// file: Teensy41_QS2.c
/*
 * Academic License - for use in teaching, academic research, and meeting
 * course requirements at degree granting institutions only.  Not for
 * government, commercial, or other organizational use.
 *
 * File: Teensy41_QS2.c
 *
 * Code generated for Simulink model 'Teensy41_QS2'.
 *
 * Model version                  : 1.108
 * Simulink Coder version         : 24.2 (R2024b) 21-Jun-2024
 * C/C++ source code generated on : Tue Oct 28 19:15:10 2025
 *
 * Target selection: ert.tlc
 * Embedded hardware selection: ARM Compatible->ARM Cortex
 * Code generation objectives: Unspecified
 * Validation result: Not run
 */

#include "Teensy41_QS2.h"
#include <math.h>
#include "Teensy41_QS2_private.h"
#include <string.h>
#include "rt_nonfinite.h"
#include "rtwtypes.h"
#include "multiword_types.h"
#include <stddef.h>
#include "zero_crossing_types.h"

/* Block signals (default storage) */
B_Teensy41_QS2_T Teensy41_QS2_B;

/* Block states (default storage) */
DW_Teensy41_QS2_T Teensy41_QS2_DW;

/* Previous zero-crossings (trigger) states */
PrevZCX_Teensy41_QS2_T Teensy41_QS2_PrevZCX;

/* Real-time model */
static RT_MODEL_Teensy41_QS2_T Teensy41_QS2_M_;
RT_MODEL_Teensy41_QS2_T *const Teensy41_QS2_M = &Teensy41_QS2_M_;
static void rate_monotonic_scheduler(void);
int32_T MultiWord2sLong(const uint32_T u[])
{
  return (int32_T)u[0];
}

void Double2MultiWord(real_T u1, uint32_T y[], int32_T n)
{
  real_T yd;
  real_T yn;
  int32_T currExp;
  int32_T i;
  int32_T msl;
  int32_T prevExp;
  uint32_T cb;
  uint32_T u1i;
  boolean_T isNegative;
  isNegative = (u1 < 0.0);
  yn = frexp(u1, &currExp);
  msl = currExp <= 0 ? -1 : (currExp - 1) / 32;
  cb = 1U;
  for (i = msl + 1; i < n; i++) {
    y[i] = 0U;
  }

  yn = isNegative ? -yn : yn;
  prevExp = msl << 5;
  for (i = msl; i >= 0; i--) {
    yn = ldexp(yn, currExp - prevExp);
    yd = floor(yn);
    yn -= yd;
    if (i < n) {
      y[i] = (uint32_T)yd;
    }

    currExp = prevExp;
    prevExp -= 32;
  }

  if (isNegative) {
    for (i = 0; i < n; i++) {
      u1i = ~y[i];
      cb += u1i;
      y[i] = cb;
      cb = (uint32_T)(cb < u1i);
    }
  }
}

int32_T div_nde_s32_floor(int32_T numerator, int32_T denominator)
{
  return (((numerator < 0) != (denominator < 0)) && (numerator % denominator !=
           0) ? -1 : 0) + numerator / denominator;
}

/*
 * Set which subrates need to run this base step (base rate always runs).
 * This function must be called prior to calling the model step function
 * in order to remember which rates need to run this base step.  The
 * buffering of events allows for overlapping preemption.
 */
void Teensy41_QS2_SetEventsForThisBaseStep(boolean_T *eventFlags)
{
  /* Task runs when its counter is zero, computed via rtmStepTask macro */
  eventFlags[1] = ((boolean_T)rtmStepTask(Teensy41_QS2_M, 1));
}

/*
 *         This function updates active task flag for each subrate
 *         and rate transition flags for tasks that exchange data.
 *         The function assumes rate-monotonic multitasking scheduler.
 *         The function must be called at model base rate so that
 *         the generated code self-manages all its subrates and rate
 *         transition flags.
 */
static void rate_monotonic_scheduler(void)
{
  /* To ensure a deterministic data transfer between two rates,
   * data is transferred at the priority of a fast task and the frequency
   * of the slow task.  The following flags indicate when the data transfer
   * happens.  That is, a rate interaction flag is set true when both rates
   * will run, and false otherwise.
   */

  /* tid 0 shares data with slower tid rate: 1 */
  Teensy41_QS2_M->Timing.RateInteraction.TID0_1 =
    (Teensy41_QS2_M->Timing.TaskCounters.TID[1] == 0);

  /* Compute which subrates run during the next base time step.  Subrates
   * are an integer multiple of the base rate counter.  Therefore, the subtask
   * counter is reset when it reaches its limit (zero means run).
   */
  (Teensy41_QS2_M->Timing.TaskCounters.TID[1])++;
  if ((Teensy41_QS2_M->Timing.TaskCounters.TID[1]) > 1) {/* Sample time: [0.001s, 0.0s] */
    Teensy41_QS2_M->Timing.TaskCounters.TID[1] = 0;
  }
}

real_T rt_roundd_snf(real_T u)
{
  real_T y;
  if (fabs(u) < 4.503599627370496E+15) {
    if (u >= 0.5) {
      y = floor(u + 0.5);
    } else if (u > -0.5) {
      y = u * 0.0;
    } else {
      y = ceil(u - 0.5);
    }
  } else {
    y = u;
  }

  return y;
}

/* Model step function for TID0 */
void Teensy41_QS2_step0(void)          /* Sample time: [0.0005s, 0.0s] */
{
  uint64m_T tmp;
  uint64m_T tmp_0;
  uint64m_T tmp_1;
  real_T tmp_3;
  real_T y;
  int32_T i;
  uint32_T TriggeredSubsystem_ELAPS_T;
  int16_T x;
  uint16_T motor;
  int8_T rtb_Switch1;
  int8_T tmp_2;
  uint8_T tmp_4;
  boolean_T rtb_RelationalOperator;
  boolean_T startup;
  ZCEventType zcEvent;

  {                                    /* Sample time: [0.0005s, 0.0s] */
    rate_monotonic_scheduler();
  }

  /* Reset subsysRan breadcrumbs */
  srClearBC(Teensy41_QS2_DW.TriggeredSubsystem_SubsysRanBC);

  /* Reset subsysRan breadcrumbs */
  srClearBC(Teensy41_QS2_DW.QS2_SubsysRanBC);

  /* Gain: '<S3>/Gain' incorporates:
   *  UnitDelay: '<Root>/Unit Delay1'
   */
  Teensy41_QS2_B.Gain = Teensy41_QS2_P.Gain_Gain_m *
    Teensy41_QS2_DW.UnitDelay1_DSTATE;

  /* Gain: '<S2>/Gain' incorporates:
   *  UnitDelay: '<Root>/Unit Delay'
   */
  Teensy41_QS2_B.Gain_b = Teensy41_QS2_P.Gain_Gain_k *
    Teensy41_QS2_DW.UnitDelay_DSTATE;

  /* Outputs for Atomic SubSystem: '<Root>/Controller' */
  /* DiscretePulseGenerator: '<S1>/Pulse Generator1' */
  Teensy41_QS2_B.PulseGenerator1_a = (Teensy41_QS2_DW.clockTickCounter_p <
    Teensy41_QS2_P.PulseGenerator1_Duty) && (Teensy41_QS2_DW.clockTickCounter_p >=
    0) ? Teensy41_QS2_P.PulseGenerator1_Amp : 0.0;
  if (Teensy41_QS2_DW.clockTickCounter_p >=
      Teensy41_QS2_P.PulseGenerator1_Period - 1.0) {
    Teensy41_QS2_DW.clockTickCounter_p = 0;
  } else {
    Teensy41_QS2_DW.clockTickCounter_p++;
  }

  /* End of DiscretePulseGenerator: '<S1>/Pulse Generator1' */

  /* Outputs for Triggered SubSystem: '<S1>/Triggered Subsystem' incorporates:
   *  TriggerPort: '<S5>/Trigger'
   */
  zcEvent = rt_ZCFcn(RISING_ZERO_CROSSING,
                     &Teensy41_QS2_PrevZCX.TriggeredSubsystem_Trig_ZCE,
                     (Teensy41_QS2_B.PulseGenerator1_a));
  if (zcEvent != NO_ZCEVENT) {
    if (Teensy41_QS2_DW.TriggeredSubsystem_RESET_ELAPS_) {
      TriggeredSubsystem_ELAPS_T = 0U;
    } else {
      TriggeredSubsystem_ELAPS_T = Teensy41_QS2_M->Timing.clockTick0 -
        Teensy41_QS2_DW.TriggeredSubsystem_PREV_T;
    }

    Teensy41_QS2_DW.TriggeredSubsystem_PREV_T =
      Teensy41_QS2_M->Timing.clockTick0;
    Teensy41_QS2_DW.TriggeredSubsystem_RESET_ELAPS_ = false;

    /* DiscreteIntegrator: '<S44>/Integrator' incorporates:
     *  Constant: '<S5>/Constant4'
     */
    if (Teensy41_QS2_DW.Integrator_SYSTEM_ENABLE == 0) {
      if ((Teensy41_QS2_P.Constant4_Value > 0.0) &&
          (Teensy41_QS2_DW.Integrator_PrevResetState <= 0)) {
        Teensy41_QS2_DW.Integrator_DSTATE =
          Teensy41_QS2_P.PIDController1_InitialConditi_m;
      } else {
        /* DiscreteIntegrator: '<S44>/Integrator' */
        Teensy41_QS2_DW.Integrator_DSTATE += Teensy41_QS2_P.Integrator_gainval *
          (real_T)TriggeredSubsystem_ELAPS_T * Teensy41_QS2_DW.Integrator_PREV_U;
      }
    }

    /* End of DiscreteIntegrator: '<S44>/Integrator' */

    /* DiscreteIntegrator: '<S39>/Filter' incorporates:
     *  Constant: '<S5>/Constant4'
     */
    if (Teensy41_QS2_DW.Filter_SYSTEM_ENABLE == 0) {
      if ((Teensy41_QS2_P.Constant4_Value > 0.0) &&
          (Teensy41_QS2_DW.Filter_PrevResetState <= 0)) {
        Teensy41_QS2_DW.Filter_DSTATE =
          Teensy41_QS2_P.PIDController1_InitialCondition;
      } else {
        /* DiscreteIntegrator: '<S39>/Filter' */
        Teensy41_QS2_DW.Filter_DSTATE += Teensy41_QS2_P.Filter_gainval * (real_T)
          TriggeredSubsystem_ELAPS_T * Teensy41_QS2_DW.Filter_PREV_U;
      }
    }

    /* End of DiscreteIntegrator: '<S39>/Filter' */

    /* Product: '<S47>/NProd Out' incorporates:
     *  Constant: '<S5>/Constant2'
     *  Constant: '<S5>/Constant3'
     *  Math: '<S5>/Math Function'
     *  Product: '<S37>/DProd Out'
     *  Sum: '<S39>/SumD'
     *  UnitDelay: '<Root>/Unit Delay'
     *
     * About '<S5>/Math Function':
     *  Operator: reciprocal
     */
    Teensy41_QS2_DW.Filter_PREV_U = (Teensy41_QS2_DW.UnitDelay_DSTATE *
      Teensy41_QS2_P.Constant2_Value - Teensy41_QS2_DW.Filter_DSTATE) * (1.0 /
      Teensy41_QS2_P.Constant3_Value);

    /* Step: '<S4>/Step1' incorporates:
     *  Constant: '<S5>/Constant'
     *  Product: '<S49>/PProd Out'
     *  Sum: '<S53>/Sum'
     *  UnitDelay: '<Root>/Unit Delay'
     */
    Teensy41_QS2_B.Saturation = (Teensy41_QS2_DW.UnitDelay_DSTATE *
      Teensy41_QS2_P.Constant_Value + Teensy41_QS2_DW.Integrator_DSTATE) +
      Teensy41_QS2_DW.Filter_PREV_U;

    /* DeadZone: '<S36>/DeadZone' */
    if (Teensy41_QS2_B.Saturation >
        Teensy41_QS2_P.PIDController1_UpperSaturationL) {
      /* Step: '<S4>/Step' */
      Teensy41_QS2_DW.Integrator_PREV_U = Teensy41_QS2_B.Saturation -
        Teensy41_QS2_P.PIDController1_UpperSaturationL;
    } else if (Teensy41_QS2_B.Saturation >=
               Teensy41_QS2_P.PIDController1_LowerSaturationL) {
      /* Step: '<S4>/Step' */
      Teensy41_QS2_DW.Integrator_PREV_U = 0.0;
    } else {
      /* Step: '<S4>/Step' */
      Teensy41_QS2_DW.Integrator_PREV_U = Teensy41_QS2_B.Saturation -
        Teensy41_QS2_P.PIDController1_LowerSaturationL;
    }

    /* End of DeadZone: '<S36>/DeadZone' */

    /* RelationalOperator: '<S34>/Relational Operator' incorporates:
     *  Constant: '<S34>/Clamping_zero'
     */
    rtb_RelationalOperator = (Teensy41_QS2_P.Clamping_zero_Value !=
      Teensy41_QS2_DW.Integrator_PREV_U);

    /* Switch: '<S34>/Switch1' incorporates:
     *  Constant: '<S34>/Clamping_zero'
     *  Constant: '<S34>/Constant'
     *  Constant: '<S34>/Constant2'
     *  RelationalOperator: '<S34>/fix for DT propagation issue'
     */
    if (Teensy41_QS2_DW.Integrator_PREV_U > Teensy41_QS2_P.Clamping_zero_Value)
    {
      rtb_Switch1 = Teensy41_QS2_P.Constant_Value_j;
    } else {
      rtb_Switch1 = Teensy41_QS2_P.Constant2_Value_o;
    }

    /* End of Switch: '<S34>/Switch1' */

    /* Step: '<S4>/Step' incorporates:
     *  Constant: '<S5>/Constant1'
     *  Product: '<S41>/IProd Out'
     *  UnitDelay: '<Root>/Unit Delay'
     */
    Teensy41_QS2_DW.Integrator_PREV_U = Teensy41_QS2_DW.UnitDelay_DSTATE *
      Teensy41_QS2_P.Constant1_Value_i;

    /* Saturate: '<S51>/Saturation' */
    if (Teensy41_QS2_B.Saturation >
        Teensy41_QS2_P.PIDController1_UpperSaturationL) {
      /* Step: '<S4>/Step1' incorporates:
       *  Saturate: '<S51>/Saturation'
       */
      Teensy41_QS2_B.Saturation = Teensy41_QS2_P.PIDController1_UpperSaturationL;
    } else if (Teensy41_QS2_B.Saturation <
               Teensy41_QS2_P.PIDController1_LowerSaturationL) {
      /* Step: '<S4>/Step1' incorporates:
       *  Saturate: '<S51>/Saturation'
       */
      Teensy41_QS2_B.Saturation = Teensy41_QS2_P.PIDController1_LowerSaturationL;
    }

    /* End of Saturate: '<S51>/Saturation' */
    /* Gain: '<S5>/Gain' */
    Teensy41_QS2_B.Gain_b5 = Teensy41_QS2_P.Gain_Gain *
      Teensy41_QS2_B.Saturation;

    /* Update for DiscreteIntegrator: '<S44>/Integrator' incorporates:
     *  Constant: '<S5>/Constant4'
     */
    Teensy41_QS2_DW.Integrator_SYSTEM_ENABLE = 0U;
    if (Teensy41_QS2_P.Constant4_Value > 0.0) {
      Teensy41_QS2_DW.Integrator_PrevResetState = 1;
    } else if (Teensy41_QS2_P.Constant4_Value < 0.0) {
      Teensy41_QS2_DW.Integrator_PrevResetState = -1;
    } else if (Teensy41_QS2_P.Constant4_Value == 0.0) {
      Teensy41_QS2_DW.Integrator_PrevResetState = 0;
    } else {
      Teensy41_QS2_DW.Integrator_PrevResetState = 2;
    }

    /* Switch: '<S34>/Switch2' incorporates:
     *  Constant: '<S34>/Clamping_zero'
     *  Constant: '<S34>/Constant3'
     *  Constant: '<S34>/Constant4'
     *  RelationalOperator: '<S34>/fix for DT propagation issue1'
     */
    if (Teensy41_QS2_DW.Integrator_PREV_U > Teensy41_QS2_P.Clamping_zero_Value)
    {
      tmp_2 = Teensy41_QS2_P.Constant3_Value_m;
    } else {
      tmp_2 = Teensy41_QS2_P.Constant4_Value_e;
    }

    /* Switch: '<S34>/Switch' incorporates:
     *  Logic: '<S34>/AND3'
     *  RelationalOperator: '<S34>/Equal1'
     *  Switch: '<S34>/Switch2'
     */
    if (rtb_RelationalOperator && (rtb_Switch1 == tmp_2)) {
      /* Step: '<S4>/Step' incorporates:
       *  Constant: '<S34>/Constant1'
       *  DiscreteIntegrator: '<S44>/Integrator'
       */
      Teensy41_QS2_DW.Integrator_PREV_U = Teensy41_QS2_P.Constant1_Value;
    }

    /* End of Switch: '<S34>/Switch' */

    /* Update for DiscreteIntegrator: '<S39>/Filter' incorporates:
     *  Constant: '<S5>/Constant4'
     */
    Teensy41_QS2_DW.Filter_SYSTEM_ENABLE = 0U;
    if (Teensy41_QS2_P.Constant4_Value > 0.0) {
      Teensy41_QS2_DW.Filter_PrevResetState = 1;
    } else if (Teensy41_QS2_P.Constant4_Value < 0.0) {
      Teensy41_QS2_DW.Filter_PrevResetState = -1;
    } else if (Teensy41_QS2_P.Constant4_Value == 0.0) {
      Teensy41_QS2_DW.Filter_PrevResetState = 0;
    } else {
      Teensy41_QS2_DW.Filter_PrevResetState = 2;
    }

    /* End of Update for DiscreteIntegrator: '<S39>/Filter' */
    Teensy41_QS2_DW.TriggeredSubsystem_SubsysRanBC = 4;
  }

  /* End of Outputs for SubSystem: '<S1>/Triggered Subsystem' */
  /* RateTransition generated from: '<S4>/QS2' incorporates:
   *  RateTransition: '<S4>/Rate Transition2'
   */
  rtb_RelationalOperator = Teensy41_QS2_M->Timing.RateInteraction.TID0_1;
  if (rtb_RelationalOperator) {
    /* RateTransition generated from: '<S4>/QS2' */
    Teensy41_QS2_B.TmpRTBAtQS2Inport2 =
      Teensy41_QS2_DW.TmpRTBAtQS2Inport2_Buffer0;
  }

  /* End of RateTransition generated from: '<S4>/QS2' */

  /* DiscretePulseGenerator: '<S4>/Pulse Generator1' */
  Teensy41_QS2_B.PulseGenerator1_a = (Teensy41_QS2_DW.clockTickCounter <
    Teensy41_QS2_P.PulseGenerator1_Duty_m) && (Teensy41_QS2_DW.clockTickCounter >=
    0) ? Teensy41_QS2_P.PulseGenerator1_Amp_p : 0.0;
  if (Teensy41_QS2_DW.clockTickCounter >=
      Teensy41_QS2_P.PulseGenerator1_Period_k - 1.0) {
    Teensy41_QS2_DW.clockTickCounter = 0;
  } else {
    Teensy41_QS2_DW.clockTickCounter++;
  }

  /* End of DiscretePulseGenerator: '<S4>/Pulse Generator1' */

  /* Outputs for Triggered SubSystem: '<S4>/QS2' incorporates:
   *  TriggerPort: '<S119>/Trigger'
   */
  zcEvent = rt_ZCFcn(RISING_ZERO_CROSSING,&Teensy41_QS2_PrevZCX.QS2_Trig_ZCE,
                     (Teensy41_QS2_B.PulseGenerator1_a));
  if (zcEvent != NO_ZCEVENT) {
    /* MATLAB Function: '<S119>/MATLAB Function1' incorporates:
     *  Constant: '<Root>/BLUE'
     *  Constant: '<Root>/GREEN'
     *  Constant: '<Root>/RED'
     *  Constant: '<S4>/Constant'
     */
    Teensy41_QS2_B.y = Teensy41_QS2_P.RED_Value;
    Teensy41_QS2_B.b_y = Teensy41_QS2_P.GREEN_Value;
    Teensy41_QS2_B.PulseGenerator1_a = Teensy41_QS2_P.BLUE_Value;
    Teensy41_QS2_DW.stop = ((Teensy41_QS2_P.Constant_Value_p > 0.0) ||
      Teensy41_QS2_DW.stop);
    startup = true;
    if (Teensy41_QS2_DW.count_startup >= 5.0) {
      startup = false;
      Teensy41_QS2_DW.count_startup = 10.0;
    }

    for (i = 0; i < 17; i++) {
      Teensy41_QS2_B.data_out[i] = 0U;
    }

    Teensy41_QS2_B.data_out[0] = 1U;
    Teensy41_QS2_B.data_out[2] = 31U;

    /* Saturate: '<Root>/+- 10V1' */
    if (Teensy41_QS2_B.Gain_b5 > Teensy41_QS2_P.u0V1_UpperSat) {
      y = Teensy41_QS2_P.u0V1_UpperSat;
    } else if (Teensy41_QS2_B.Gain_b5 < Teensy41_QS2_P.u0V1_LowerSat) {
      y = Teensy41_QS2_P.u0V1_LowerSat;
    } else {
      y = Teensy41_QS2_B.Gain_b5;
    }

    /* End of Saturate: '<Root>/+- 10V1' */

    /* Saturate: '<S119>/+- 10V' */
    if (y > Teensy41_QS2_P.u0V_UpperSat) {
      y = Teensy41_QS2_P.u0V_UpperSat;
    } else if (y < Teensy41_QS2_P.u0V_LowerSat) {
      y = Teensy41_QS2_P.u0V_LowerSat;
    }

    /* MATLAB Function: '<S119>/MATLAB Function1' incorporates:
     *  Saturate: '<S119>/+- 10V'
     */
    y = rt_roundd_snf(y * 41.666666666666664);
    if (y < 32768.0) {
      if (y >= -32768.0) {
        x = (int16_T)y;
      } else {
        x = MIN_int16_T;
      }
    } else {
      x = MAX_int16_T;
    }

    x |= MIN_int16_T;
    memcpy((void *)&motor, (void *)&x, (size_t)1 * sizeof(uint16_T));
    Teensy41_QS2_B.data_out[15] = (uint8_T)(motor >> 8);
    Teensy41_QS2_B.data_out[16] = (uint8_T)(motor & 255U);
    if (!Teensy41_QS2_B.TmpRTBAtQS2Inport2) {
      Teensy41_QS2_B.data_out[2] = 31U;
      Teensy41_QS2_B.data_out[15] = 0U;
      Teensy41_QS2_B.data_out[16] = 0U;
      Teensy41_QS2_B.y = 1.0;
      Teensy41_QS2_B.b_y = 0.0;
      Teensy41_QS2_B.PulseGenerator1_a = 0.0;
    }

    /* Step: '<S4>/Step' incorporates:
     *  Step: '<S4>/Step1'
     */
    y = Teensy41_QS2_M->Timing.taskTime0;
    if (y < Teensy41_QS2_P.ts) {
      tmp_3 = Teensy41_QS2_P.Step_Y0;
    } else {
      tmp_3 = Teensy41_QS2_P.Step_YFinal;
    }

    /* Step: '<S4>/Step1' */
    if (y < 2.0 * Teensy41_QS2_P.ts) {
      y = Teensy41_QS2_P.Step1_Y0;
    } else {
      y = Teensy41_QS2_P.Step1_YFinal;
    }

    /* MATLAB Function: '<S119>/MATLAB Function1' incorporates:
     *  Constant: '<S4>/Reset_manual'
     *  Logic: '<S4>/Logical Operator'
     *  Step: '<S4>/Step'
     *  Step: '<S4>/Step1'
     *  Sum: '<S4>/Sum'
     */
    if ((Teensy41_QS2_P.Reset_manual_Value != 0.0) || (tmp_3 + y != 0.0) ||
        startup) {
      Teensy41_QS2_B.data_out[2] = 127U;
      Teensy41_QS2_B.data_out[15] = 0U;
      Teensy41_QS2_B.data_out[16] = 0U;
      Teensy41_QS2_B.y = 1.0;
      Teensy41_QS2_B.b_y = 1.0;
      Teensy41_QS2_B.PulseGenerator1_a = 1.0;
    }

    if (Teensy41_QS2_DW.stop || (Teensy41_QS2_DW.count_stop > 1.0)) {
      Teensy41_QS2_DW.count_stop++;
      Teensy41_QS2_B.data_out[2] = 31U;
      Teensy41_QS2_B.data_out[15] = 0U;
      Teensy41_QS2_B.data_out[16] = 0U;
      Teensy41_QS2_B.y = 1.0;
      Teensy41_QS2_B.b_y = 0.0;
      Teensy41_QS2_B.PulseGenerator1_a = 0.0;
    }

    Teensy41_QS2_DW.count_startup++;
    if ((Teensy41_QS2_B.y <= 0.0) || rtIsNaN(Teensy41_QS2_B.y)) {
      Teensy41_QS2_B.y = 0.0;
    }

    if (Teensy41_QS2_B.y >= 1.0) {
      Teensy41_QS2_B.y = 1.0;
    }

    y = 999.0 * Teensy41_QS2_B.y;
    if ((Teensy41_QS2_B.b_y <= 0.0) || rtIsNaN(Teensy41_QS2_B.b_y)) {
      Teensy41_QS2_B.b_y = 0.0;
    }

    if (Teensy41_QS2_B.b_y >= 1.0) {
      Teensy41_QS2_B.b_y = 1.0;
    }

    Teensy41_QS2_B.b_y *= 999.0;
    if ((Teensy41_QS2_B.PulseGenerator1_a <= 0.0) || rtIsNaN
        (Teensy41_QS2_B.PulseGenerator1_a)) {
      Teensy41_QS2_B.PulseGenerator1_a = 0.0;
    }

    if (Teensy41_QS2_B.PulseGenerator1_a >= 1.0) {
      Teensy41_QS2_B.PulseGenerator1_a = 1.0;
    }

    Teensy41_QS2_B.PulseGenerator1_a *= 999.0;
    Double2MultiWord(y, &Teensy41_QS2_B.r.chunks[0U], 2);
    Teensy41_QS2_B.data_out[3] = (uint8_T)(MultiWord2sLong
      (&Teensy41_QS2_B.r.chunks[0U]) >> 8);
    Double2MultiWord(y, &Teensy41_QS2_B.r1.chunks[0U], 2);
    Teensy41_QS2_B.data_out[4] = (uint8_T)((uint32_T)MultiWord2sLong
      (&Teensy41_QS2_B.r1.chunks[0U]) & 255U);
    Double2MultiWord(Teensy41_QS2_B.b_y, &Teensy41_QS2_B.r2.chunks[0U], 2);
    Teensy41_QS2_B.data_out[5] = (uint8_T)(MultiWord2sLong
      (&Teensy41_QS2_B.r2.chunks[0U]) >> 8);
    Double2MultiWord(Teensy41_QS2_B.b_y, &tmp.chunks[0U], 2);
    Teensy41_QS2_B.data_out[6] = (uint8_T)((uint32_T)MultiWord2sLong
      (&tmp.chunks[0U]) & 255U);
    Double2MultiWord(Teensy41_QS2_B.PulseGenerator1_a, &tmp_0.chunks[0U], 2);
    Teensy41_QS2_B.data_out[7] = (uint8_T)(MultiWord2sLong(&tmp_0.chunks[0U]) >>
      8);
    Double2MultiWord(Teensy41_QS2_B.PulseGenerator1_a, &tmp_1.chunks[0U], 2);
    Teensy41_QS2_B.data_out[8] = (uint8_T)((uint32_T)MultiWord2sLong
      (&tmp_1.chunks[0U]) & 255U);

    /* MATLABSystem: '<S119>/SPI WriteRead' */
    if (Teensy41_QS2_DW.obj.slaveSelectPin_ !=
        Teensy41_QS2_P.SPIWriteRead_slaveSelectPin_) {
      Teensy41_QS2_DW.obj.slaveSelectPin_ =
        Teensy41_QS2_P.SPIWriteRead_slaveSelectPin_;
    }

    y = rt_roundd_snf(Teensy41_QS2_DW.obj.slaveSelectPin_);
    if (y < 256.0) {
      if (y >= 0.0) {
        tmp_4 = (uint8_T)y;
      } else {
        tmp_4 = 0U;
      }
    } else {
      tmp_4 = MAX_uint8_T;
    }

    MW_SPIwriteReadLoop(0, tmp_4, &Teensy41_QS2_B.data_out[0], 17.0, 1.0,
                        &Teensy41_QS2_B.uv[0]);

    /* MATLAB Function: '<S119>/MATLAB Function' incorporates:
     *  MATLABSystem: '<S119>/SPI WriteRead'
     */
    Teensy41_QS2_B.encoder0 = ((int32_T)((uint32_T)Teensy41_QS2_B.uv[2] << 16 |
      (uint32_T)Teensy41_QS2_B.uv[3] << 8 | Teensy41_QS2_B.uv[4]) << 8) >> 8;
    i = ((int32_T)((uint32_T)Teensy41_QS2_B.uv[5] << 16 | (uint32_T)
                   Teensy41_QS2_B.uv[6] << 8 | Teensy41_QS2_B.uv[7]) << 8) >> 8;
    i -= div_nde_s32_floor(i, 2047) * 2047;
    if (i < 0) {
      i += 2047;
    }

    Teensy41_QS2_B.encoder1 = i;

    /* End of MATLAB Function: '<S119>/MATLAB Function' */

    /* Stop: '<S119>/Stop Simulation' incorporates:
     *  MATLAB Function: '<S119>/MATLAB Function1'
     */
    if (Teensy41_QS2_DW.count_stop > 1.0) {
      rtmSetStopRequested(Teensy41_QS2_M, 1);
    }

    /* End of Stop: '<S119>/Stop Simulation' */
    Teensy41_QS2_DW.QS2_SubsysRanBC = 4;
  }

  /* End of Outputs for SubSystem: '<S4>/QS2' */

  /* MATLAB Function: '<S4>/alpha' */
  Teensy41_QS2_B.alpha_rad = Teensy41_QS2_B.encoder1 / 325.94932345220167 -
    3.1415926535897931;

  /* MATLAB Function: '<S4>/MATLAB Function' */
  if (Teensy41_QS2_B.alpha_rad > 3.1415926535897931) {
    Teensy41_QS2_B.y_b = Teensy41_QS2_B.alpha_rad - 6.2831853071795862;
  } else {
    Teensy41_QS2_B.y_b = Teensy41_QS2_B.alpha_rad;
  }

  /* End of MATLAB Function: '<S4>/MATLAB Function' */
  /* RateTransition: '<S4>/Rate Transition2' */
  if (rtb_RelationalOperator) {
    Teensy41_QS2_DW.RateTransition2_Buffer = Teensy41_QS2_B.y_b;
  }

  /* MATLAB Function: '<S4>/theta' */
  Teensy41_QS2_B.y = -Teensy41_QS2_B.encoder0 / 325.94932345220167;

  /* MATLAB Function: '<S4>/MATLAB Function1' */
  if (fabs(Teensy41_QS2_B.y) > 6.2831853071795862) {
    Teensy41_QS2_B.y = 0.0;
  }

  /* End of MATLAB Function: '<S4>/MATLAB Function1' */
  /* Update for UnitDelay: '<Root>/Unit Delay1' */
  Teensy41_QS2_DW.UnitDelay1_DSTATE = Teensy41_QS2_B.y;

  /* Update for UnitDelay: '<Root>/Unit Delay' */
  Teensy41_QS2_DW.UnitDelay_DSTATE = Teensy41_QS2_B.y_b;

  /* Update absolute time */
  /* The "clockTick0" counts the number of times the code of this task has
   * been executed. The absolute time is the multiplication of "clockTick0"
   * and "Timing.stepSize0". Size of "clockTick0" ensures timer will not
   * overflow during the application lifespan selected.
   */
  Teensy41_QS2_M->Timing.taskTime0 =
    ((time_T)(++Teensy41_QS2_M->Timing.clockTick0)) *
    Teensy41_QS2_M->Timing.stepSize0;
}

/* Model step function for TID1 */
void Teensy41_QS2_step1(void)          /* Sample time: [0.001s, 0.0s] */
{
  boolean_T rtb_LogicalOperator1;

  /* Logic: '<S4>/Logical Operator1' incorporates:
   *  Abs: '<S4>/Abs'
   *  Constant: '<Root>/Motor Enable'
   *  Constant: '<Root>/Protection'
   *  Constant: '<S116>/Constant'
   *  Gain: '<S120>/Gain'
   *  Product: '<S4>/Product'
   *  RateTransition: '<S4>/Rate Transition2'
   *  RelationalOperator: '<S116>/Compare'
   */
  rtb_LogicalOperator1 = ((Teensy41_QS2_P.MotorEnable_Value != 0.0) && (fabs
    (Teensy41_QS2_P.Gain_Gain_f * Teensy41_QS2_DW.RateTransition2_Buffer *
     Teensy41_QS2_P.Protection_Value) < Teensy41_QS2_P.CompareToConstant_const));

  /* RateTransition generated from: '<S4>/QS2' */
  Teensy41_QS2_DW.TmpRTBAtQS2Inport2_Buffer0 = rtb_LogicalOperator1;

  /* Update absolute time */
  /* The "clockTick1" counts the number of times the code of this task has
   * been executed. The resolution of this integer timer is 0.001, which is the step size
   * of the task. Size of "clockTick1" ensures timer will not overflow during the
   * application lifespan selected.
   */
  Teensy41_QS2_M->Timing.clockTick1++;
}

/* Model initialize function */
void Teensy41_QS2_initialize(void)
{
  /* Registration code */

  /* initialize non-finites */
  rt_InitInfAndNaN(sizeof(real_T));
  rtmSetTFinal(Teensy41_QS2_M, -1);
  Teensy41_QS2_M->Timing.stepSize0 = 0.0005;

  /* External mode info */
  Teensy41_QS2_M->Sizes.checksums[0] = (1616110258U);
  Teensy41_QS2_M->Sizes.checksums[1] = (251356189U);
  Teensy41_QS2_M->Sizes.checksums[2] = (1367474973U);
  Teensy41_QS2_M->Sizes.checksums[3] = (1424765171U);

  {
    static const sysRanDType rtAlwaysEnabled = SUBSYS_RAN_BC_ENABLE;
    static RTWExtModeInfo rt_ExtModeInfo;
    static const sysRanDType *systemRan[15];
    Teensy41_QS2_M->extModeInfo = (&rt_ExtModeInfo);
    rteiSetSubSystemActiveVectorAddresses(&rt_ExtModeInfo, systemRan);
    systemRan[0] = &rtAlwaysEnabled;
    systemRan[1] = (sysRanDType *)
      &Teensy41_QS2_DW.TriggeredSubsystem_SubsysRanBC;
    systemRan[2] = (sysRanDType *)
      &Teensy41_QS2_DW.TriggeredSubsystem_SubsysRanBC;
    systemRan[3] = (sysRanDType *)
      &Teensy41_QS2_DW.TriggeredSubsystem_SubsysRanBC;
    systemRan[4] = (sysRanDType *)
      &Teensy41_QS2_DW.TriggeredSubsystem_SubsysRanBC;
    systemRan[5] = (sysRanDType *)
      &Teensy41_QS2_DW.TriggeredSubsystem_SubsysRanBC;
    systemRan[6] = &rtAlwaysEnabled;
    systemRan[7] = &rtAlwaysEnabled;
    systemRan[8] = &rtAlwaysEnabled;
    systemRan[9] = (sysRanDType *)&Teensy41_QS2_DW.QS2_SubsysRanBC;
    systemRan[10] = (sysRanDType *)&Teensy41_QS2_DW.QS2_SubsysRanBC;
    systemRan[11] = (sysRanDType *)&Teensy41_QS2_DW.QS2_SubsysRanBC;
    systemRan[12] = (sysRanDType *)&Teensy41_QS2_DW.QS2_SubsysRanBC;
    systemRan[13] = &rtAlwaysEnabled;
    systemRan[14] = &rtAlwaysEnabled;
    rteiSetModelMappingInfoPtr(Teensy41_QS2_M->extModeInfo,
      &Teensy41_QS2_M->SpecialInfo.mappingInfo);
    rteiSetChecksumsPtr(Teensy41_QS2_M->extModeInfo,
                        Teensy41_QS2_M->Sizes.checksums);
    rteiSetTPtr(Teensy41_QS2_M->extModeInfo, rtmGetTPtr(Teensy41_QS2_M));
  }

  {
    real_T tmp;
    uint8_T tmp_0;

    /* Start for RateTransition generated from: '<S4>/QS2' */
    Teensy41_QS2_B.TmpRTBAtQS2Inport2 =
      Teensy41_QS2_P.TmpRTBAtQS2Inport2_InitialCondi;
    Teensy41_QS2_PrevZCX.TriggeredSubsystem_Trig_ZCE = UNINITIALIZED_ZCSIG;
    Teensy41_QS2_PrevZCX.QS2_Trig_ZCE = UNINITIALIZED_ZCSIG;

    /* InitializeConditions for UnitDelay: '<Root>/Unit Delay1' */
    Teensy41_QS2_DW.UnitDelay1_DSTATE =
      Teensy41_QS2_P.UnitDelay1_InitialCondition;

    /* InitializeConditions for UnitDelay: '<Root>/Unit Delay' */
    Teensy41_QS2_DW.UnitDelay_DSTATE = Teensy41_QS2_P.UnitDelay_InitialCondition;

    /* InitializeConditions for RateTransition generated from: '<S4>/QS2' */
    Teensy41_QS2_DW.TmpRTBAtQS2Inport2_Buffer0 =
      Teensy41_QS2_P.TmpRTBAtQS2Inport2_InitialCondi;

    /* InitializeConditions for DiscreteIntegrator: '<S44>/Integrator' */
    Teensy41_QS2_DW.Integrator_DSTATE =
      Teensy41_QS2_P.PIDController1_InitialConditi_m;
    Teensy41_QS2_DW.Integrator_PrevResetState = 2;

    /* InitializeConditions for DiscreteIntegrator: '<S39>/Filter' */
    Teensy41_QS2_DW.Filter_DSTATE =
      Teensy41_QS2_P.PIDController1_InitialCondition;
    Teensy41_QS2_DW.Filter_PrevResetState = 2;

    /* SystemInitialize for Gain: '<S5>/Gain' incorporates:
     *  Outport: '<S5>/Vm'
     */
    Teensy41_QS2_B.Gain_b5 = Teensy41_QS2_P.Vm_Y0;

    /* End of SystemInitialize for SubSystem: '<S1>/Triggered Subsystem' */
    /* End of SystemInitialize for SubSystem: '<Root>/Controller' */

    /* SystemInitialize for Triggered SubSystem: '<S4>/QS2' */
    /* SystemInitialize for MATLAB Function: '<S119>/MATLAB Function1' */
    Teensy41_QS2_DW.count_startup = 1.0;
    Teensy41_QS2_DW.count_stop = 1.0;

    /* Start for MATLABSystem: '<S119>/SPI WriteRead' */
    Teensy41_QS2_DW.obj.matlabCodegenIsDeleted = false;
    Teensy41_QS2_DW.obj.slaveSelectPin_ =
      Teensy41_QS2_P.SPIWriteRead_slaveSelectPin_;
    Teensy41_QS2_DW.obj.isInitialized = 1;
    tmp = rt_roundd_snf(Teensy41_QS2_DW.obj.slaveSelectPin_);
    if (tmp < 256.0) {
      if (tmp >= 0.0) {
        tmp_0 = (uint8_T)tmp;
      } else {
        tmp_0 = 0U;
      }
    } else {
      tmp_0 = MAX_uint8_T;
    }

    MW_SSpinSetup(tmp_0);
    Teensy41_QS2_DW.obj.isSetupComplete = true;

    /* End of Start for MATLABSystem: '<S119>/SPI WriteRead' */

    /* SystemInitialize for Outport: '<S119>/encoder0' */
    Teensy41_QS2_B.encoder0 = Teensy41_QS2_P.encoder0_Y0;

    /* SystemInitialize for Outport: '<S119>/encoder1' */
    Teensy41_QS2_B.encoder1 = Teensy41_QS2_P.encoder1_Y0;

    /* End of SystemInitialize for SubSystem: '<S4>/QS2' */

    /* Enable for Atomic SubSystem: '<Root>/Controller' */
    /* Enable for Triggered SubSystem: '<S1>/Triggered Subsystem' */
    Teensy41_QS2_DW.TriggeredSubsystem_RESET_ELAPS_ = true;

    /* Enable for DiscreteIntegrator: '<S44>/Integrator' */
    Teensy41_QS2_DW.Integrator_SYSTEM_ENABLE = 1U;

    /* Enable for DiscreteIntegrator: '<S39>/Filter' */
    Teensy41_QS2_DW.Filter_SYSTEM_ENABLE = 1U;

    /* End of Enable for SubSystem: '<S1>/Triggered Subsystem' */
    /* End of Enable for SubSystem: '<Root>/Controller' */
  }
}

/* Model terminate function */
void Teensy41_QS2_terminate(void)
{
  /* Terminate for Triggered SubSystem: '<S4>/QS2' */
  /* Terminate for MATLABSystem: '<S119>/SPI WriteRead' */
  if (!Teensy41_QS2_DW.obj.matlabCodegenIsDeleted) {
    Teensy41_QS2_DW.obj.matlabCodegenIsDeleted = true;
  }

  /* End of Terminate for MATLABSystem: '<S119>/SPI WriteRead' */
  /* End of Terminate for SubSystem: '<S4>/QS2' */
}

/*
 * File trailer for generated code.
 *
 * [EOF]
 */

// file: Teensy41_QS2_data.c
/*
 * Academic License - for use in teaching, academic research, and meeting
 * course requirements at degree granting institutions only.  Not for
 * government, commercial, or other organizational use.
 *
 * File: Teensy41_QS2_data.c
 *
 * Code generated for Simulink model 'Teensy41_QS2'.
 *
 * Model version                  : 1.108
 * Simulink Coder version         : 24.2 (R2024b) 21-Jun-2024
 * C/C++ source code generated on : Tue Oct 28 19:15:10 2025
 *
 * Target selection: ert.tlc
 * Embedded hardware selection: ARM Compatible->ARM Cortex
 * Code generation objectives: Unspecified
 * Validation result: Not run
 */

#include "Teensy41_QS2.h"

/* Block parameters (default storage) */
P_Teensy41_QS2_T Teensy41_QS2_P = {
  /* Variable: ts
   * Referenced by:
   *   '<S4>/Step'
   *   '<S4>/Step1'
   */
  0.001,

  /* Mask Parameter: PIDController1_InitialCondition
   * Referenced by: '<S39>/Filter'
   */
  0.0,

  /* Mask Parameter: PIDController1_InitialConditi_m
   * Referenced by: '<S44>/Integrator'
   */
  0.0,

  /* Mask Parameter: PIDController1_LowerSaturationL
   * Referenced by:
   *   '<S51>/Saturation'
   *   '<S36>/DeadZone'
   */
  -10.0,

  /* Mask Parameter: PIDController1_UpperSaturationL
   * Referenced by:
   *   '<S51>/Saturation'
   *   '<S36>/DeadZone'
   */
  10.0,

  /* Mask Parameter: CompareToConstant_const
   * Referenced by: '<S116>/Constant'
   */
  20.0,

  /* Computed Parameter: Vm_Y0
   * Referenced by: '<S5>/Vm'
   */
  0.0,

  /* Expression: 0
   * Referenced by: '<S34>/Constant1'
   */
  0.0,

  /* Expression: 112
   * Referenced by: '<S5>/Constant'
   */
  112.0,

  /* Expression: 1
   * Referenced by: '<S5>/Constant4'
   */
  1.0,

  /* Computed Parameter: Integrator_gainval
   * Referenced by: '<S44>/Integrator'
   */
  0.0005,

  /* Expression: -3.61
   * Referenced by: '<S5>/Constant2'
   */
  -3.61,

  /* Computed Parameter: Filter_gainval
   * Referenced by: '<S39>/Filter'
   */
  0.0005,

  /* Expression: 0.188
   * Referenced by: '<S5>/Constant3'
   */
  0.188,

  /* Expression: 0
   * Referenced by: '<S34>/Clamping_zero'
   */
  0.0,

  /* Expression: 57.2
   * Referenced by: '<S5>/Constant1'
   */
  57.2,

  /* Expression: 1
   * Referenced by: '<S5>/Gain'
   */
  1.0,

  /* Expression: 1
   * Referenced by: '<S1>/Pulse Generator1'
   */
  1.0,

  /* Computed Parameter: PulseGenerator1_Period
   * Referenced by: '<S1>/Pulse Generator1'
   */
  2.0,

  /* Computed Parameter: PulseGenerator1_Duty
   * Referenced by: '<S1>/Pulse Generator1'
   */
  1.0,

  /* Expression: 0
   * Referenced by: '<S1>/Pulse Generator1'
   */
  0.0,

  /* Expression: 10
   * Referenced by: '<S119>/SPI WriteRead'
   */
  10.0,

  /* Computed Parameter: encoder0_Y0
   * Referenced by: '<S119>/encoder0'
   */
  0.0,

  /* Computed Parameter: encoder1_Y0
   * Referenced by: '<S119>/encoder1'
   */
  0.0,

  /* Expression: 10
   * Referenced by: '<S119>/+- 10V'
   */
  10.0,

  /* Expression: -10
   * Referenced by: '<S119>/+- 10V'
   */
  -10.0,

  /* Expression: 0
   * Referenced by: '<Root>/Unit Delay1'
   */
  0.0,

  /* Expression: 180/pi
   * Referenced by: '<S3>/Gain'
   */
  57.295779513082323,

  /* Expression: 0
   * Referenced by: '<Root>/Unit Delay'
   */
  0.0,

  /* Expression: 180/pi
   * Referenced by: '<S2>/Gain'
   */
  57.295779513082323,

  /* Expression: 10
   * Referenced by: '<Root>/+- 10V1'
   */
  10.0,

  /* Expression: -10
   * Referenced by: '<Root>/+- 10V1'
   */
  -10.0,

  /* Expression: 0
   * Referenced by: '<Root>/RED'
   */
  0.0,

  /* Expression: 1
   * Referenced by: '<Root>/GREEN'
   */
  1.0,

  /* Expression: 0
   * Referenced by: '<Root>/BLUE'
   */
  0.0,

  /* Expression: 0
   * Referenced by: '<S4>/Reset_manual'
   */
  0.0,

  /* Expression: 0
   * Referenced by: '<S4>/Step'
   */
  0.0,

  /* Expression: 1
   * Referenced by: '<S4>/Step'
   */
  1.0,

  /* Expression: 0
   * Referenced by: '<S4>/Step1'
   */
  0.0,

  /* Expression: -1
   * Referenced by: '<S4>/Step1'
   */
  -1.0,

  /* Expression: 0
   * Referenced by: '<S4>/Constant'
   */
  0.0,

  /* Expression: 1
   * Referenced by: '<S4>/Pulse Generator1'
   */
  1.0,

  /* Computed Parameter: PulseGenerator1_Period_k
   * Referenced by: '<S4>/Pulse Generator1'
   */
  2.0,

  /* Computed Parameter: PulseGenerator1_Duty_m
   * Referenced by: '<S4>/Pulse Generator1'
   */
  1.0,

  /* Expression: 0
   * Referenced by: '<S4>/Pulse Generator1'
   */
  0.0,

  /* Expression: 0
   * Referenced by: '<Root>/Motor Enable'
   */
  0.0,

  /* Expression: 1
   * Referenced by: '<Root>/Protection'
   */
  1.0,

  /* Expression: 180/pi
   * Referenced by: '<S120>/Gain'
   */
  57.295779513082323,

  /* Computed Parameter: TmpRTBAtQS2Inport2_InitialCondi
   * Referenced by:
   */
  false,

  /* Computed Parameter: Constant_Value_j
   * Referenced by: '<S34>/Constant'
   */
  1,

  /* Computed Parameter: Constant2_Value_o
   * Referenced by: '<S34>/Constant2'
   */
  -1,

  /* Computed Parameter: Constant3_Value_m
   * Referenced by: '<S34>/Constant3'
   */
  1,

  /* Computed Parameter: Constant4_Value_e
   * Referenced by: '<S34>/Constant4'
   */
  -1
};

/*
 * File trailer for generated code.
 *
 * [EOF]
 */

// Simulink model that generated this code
simulink model "Teensy41_QS2"  (R2024b)
settings: Solver=FixedStepAuto  StartTime=0.0  StopTime=inf  RelTol=1e-3  EnableMultiTasking=on
InitFcn:
  | run('Teensy41_system_init.m');
StopFcn:
  | run('Teensy41_to_save_data.m');
values from neighbouring files (symbols this model uses):
  ts = time(2)    [RotaryPendulum.m]    (also in Teensy41_system_init.m = 0.001)
libraries: simulink_extras x3, slpidlib x2, simulink x1, arduinolib x1

== system Teensy41_QS2 ==
  note: 41277 Control Design, UTS, Australia
      |
      | Rotary Inverted Pendulum System
      | QUBE-Servo 2
      |
      | Ricardo Aguilera, Rodrigo Cuzmar, Pablo Poblete
  note: -10V to 10V
  +- 10V1 : Saturate  UpperLimit=10  LowerLimit=-10
  BLUE : Constant  Value=0
  Controller : Subsystem  TreatAsAtomicUnit=on
  GREEN : Constant
  Motor Enable : Constant  Value=0
  Protection : Constant
  Push Button : PushButtonBlock  ButtonText=Sensor Reset  OffValue=0.000000
  Push Button1 : CustomTuningWebBlock  LabelPosition=Hide  ShowInitialText=on  Configuration="{\"components\":[{\"name\":\"BackgroundImageComponent\",\"settings\":{\"image\":{\"size\":[0,0],\"src\":\"default\",\"srcOrientation\":\"horizontal\"},\"position\":[0,0,1,1],\"scaleMode\":\"0\"}},{\"name\":\"ButtonStateComponent\",\"settings\":{\"buttonType\":\"momentary\",\"clickFcn\":\"\",\"image\":{\"size\":[180,45],\"srcOrientation\":\"Right\"},\"latched\":true,\"offValue\":0,\"onValue\":\"1\",\"position\":[0,0,1,1],\"pressDelay\":\"500\",\"pressFcn\":\"\",\" ...(+13251 chars)"
  RED : Constant  Value=0
  Radians to Degrees : simulink_extras/Transformations/Radians to Degrees
  Radians to Degrees1 : simulink_extras/Transformations/Radians to Degrees
  Rocker Switch : RockerSwitchBlock
  "System:    QS2      " : Subsystem
  Terminator2 : Terminator
  Terminator3 : Terminator
  Unit Delay : UnitDelay  SampleTime=-1  HasFrameUpgradeWarning=on
  Unit Delay1 : UnitDelay  SampleTime=-1  HasFrameUpgradeWarning=on
  wires:
  Motor Enable/1 -> "System:    QS2      "/2(Enable)
  Controller/1(Vm) -> +- 10V1/1  "Vm"
  "System:    QS2      "/1(alpha_rad) -> Unit Delay/1  "alpha_rad"
  "System:    QS2      "/2(theta_rad) -> Unit Delay1/1  "theta_rad"
  RED/1 -> "System:    QS2      "/4(R_LED)
  GREEN/1 -> "System:    QS2      "/5(G_LED)
  BLUE/1 -> "System:    QS2      "/6(B_LED)
  Protection/1 -> "System:    QS2      "/3(Protection)
  Radians to Degrees/1 -> Terminator2/1  "alpha_deg"
  Radians to Degrees1/1 -> Terminator3/1  "theta_deg"
  Unit Delay/1 -> Controller/1(Alpha_Rad), Radians to Degrees/1
  Unit Delay1/1 -> Controller/2(Theta_Rad), Radians to Degrees1/1
  +- 10V1/1 -> "System:    QS2      "/1(Vm)

== system Teensy41_QS2/Controller ==
  note: Timer
      | Interrupt
  Alpha_Rad : Inport
  Theta_Rad : Inport  Port=2
  Pulse Generator1 : DiscretePulseGenerator  PulseType=Time based  Period=ts  PulseWidth=50
  Triggered Subsystem : Subsystem  TreatAsAtomicUnit=on
  Vm : Outport
  wires:
  Triggered Subsystem/1(Vm) -> Vm/1  "Vm2"
  Pulse Generator1/1 -> Triggered Subsystem/Trigger
  Alpha_Rad/1 -> Triggered Subsystem/1("Alpha_Rad ")
  Theta_Rad/1 -> Triggered Subsystem/2(Theta_Rad)

== system Teensy41_QS2/System:    QS2       ==
  note: QUEBE-Servo 2 SPI to obtain Encoders' values
  note: Sensors Reset
  note: Protection
  note: Angles
  Vm : Inport
  Enable : Inport  Port=2
  Protection : Inport  Port=3
  R_LED : Inport  Port=4
  G_LED : Inport  Port=5
  B_LED : Inport  Port=6
  Abs : Abs  SaturateOnIntegerOverflow=off
  Compare To Constant : simulink/Logic and Bit Operations/Compare To Constant  relop=<  const=20  OutDataTypeStr=boolean
  Constant : Constant  Value=0
  Logical Operator : Logic  Operator=OR  AllPortsSameDT=off  OutDataTypeStr=boolean
  Logical Operator1 : Logic  AllPortsSameDT=off  OutDataTypeStr=boolean
  MATLAB Function : MATLAB Function  TreatAsAtomicUnit=on
  MATLAB Function1 : MATLAB Function  TreatAsAtomicUnit=on
  Product : Product
  Pulse Generator1 : DiscretePulseGenerator  PulseType=Time based  Period=ts  PulseWidth=50
  QS2 : Subsystem  TreatAsAtomicUnit=on
  Radians to Degrees : simulink_extras/Transformations/Radians to Degrees
  Rate Transition2 : RateTransition  OutPortSampleTimeOpt=Multiple of input port sample time  OutPortSampleTimeMultiple=2
  Reset_manual : Constant  Value=0  SampleTime=-1
  Step : Step  Time=ts
  Step1 : Step  Time=2*ts  After=-1
  Sum : Sum  Inputs=|++
  alpha : MATLAB Function  TreatAsAtomicUnit=on
  theta : MATLAB Function  TreatAsAtomicUnit=on
  alpha_rad : Outport
  theta_rad : Outport  Port=2
  tag scope: Enable=global, Reset=global, SIM_STOP=global, theta_rad=global
  wires:
  Reset_manual/1 -> Logical Operator/1
  Logical Operator/1 -> [Reset]
  Step/1 -> Sum/1
  Step1/1 -> Sum/2
  Sum/1 -> Logical Operator/2
  Pulse Generator1/1 -> QS2/Trigger
  [Reset] -> QS2/6(Reset)
  Vm/1 -> QS2/1(Vm)
  R_LED/1 -> QS2/3(R_LED)
  B_LED/1 -> QS2/5(B_LED)
  G_LED/1 -> QS2/4(G_LED)
  [SIM_STOP] -> QS2/7(STOP)
  Constant/1 -> [SIM_STOP]
  Abs/1 -> Compare To Constant/1
  [Enable] -> QS2/2(Enable)
  QS2/1(encoder0) -> theta/1(encoder0)
  Rate Transition2/1 -> Radians to Degrees/1
  Logical Operator1/1 -> [Enable]
  Compare To Constant/1 -> Logical Operator1/2
  Enable/1 -> Logical Operator1/1
  Protection/1 -> Product/2
  QS2/2(encoder1) -> alpha/1(encoder1)
  Product/1 -> Abs/1
  [theta_rad] -> Rate Transition2/1
  Radians to Degrees/1 -> Product/1
  MATLAB Function1/1(y) -> theta_rad/1
  theta/1(theta_rad) -> MATLAB Function1/1(u)
  alpha/1(alpha_rad) -> MATLAB Function/1(u)  "Pre_pi"
  MATLAB Function/1(y) -> [theta_rad], alpha_rad/1  "asd"

== system Teensy41_QS2/Controller/Triggered Subsystem ==
  "Alpha_Rad " : Inport
  Theta_Rad : Inport  Port=2
  Trigger : TriggerPort  VariantControl=(inherit)  ShowOutputPort=on
  Gain : Gain  Gain=-1
  PID Controller1 : slpidlib/PID Controller  Controller=PID  Form=Parallel  TimeDomain=Discrete-time  UseExternalTs=on  SampleTime=ts  IntegratorMethod=Forward Euler  FilterMethod=Forward Euler  ControllerParametersSource=internal  P=-79.8  I=-174  UseKiTs=off  D=-13.1  UseExternalDerivativeSource=off  N=1/0.00466  UseFilter=on  TunerSelectOption=Transfer Function Based (PID Tuner App)  InitialConditionSource=internal  InitialConditionForIntegrator=0  InitialConditionForFilter=0  DifferentiatorICPrevScaledInput=0  ExternalReset=none  TrackingMode=off  Kt=1  LimitOutput=off  SatLimitsSource=internal  UpperSaturationLimit=inf  LowerSaturationLimit=-inf  LinearizeAsGain=on  AntiWindupMode=none  Kb=1  LimitIntegrator=off  UpperIntegratorSaturationLimit=inf  LowerIntegratorSaturationLimit=-inf  POutMin=[]  POutMax=[]  IOutMin=[]  IOutMax=[]  DOutMin=[]  DOutMax=[]  NOutMin=[]  NOutMax=[]  SumOutMin=[]  SumOutMax=[]  SaturationOutMin=[]  SaturationOutMax=[]  PParamMin=[]  PParamMax=[]  IParamMin=[]  IParamMax=[]  DParamMin=[]  DParamMax=[]  NParamMin=[]  NParamMax=[]  KbParamMin=[]  KbParamMax=[]  KtParamMin=[]  KtParamMax=[]  KbOutMin=[]  KbOutMax=[]  KtOutMin=[]  KtOutMax=[]  IntegratorOutMin=[]  IntegratorOutMax=[]  FilterOutMin=[]  FilterOutMax=[]  SumI1OutMin=[]  SumI1OutMax=[]  SumI2OutMin=[]  SumI2OutMax=[]  SumI3OutMin=[]  SumI3OutMax=[]  SumI4OutMin=[]  SumI4OutMax=[]  SumDOutMin=[]  SumDOutMax=[]  DifferentiatorOutMin=[]  DifferentiatorOutMax=[]  FilterDiffOutCoefMin=[]  FilterDiffOutCoefMax=[]  ReciprocalOutMin=[]  ReciprocalOutMax=[]  SumDenOutMin=[]  SumDenOutMax=[]  SumNumOutMin=[]  SumNumOutMax=[]  DivideOutMin=[]  DivideOutMax=[]  UdiffTsProdOutMin=[]  UdiffTsProdOutMax=[]  NTsProdOutMin=[]  NTsProdOutMax=[]  UintegralTsProdOutMin=[]  UintegralTsProdOutMax=[]  UngainTsProdOutMin=[]  UngainTsProdOutMax=[]  ClampingZeroOutDataTypeStr=Inherit: Inherit via back propagation  ClampingZeroOutMin=[]  ClampingZeroOutMax=[]  FilterDenConstantOutDataTypeStr=Inherit: Inherit via back propagation  FilterDenConstantOutMin=[]  FilterDenConstantOutMax=[]  PCopyOutDataTypeStr=Inherit: Inherit via back propagation  PCopyOutMin=[]  PCopyOutMax=[]  NCopyOutDataTypeStr=Inherit: Inherit via back propagation  NCopyOutMin=[]  NCopyOutMax=[]  IntegratorContinuousStateAttributes=''  IntegratorStateMustResolveToSignalObject=off  IntegratorRTWStateStorageClass=Auto  FilterContinuousStateAttributes=''  FilterStateMustResolveToSignalObject=off  FilterRTWStateStorageClass=Auto  ParallelPVariant=InternalParameters  IdealPVariant=Disabled  IVariant=InternalParameters  DVariant=InternalParameters  IntegratorVariant=Discrete  SatVariant=Disabled  AWVariant=Passthrough  PCopyVariant=Disabled  TRVariant=Disabled  FdbkBlocksVariant=Forward  IdealPFdbkVariant=Disabled  SatFdbkVariant=Disabled  DerivativeFilterVariant=ForwardEulerFilter  NVariant=InternalParameters  NCopyVariant=Disabled  FilterICVariant=InternalICsFilter  IntegratorICVariant=InternalICs  ExternalResetVariant=Disabled  TRSumVariant=Passthrough  SumFdbkVariant=Disabled  SumVariant=Sum_PID  TsampFilterVariant=ExternalTs  TsampNgainVariant=ExternalTs  TsampIntegralVariant=ExternalTs  ExternalSaturationOutDataTypeStr=Inherit: Same as second input  DerivativeSourceVariant=ErrorSignal  PreIntVariant=InternalPreInt
  PID Controller2 : slpidlib/PID Controller  Controller=PD  Form=Parallel  TimeDomain=Discrete-time  UseExternalTs=on  SampleTime=0.001  IntegratorMethod=Forward Euler  FilterMethod=Forward Euler  ControllerParametersSource=internal  P=-2  I=24  UseKiTs=off  D=-2  UseExternalDerivativeSource=off  N=0.5263  UseFilter=off  TunerSelectOption=Transfer Function Based (PID Tuner App)  InitialConditionSource=internal  InitialConditionForIntegrator=0  InitialConditionForFilter=0  DifferentiatorICPrevScaledInput=0  ExternalReset=none  TrackingMode=off  Kt=1  LimitOutput=off  SatLimitsSource=internal  UpperSaturationLimit=inf  LowerSaturationLimit=-inf  LinearizeAsGain=on  AntiWindupMode=none  Kb=1  LimitIntegrator=off  UpperIntegratorSaturationLimit=inf  LowerIntegratorSaturationLimit=-inf  POutMin=[]  POutMax=[]  IOutMin=[]  IOutMax=[]  DOutMin=[]  DOutMax=[]  NOutMin=[]  NOutMax=[]  SumOutMin=[]  SumOutMax=[]  SaturationOutMin=[]  SaturationOutMax=[]  PParamMin=[]  PParamMax=[]  IParamMin=[]  IParamMax=[]  DParamMin=[]  DParamMax=[]  NParamMin=[]  NParamMax=[]  KbParamMin=[]  KbParamMax=[]  KtParamMin=[]  KtParamMax=[]  KbOutMin=[]  KbOutMax=[]  KtOutMin=[]  KtOutMax=[]  IntegratorOutMin=[]  IntegratorOutMax=[]  FilterOutMin=[]  FilterOutMax=[]  SumI1OutMin=[]  SumI1OutMax=[]  SumI2OutMin=[]  SumI2OutMax=[]  SumI3OutMin=[]  SumI3OutMax=[]  SumI4OutMin=[]  SumI4OutMax=[]  SumDOutMin=[]  SumDOutMax=[]  DifferentiatorOutMin=[]  DifferentiatorOutMax=[]  FilterDiffOutCoefMin=[]  FilterDiffOutCoefMax=[]  ReciprocalOutMin=[]  ReciprocalOutMax=[]  SumDenOutMin=[]  SumDenOutMax=[]  SumNumOutMin=[]  SumNumOutMax=[]  DivideOutMin=[]  DivideOutMax=[]  UdiffTsProdOutMin=[]  UdiffTsProdOutMax=[]  NTsProdOutMin=[]  NTsProdOutMax=[]  UintegralTsProdOutMin=[]  UintegralTsProdOutMax=[]  UngainTsProdOutMin=[]  UngainTsProdOutMax=[]  ClampingZeroOutDataTypeStr=Inherit: Inherit via back propagation  ClampingZeroOutMin=[]  ClampingZeroOutMax=[]  FilterDenConstantOutDataTypeStr=Inherit: Inherit via back propagation  FilterDenConstantOutMin=[]  FilterDenConstantOutMax=[]  PCopyOutDataTypeStr=Inherit: Inherit via back propagation  PCopyOutMin=[]  PCopyOutMax=[]  NCopyOutDataTypeStr=Inherit: Inherit via back propagation  NCopyOutMin=[]  NCopyOutMax=[]  IntegratorContinuousStateAttributes=''  IntegratorStateMustResolveToSignalObject=off  IntegratorRTWStateStorageClass=Auto  FilterContinuousStateAttributes=''  FilterStateMustResolveToSignalObject=off  FilterRTWStateStorageClass=Auto  ParallelPVariant=InternalParameters  IdealPVariant=Disabled  IVariant=Disabled  DVariant=InternalParameters  IntegratorVariant=Disabled  SatVariant=Disabled  AWVariant=Disabled  PCopyVariant=Disabled  TRVariant=Disabled  FdbkBlocksVariant=Forward  IdealPFdbkVariant=Disabled  SatFdbkVariant=Disabled  DerivativeFilterVariant=Differentiator  NVariant=Passthrough  NCopyVariant=Disabled_SignalSpec  FilterICVariant=InternalICsDifferentiator  IntegratorICVariant=Disabled  ExternalResetVariant=Disabled  TRSumVariant=Passthrough  SumFdbkVariant=Disabled  SumVariant=Sum_PD  TsampFilterVariant=ExternalTs  TsampNgainVariant=Passthrough  TsampIntegralVariant=Disabled  ExternalSaturationOutDataTypeStr=Inherit: Same as second input  DerivativeSourceVariant=ErrorSignal  PreIntVariant=InternalPreInt
  Vm : Outport
  wires:
  "Alpha_Rad "/1 -> PID Controller1/1
  Trigger/1 -> PID Controller1/2, PID Controller2/2
  Theta_Rad/1 -> PID Controller2/1
  PID Controller1/1 -> Gain/1  "Vm3"
  Gain/1 -> Vm/1

== system Teensy41_QS2/System:    QS2      /QS2 ==
  Vm : Inport
  Enable : Inport  Port=2
  R_LED : Inport  Port=3
  G_LED : Inport  Port=4
  B_LED : Inport  Port=5
  Reset : Inport  Port=6
  STOP : Inport  Port=7
  Trigger : TriggerPort  VariantControl=(inherit)
  +- 10V : Saturate  UpperLimit=10  LowerLimit=-10
  MATLAB Function : MATLAB Function  TreatAsAtomicUnit=on
  MATLAB Function1 : MATLAB Function  TreatAsAtomicUnit=on
  SPI WriteRead : arduinolib/SPI WriteRead  SPIModule=0  slaveSelectPin_=10  blockPlatform=ARDUINO
  Stop Simulation : Stop
  encoder0 : Outport
  encoder1 : Outport  Port=2
  wires:
  Enable/1 -> MATLAB Function1/2(Enable)
  G_LED/1 -> MATLAB Function1/4(G_LED)
  MATLAB Function1/1(data_out) -> SPI WriteRead/1
  Vm/1 -> +- 10V/1
  R_LED/1 -> MATLAB Function1/3(R_LED)
  B_LED/1 -> MATLAB Function1/5(B_LED)
  Reset/1 -> MATLAB Function1/6(Reset)
  +- 10V/1 -> MATLAB Function1/1(Vm)
  STOP/1 -> MATLAB Function1/7(STOP)
  MATLAB Function1/2(stop_sim) -> Stop Simulation/1
  SPI WriteRead/1 -> MATLAB Function/1(data_in)
  MATLAB Function/1(encoder0) -> encoder0/1
  MATLAB Function/2(encoder1) -> encoder1/1

== matlab function Teensy41_QS2/System:    QS2      /QS2/MATLAB Function1 ==
function [data_out,stop_sim]  = QS2_SPI_write(Vm,Enable,R_LED,G_LED,B_LED,Reset, STOP)

persistent count_startup count_stop stop
if isempty(count_startup)
    count_startup = 1; 
    count_stop = 1;
    stop = false;
end

if (STOP > 0)
    stop = true;
end

startup = true;
if (count_startup>=5)
    startup = false;
    count_startup = 10;
end

%% SPI data to be sent
SPI_data_out = uint8(zeros(17,1));
SPI_data_out(1) = 1;
writeMask = 31;
SPI_data_out(3) = writeMask;

%% Motor Voltage
Vm_int = int16(Vm *(625.0 / 15.0));
Vm_int = bitset(Vm_int,16);
motor = typecast(Vm_int,'uint16');
motorMSB = bitshift(motor,-8);
motorLSB = bitand(motor,255);

SPI_data_out(16) = motorMSB;
SPI_data_out(17) = motorLSB;

%% Enable
if (Enable~=1)
    writeMask = 31;
    SPI_data_out(3) = writeMask;
    SPI_data_out(16) = 0;
    SPI_data_out(17) = 0;
    R_LED = 1;
    G_LED = 0;
    B_LED = 0;
end

%% Reset Encoders
if (Reset==1 || startup)
    writeMask = 127;
    SPI_data_out(3) = writeMask;
    SPI_data_out(16) = 0;
    SPI_data_out(17) = 0;
    R_LED = 1;
    G_LED = 1;
    B_LED = 1;
end

stop_sim = false;
if (stop || count_stop>1)
    count_stop = count_stop + 1;
    writeMask = 31;
    SPI_data_out(3) = writeMask;
    SPI_data_out(16) = 0;
    SPI_data_out(17) = 0;
    R_LED = 1;
    G_LED = 0;
    B_LED = 0;
end

if (count_stop> 1)
    stop_sim = true;
end

count_startup = count_startup + 1;

%% LEDs
R_LED = 999*min(1, max(0, R_LED));
G_LED = 999*min(1, max(0, G_LED));
B_LED = 999*min(1, max(0, B_LED));

LEDRedMSB   = bitshift(R_LED,-8);
LEDRedLSB   = bitand(R_LED, 255);
LEDGreenMSB = bitshift(G_LED,-8);
LEDGreenLSB = bitand(G_LED, 255);
LEDBlueMSB  = bitshift(B_LED,-8);
LEDBlueLSB  = bitand(B_LED, 255);

SPI_data_out(4) = LEDRedMSB;
SPI_data_out(5) = LEDRedLSB;
SPI_data_out(6) = LEDGreenMSB;
SPI_data_out(7) = LEDGreenLSB;
SPI_data_out(8) = LEDBlueMSB;
SPI_data_out(9) = LEDBlueLSB;

data_out = SPI_data_out;

== matlab function Teensy41_QS2/System:    QS2      /alpha ==
function alpha_rad = enc2alpha(encoder1)
%calibrate this angle sensor

% encoder provides 2048 counts per rotation
% when encoder1 = 0 --> alpha = -pi

% Convert E1 counts to pendulum angle (radians)
alpha_rad = (encoder1/(2048/(2*pi)))-pi;
% alpha_rad = alpha_rad - pi;

== matlab function Teensy41_QS2/System:    QS2      /MATLAB Function ==
function y = fcn(u)

y = u - pi;
if u > pi
    y = u-2*pi;
else
    y = u;
end

== matlab function Teensy41_QS2/System:    QS2      /theta ==
function theta_rad = enc2theta(encoder0)
%calibrate this angle sensor

% encoder provides 2048 counts per rotation
% when encoder0 = 0 --> alpha = 0
% negative rotation

% Convert E0 counts to rotation angle (radians)
theta_rad = -encoder0/(2048/(2*pi));

== matlab function Teensy41_QS2/System:    QS2      /MATLAB Function1 ==
function y = fcn(u)

if abs(u) > 2*pi
    u = 0;
end

y = u;

== matlab function Teensy41_QS2/System:    QS2      /QS2/MATLAB Function ==
function [encoder0, encoder1] =  QS2_SPI_read(data_in)

%% Encoder 0

%encoder0 data
encoder0Byte = [data_in(5), data_in(4), data_in(3)];

% Build 24-bit value
enc24 = bitor( ...
          bitor(bitshift(uint32(encoder0Byte(3)),16), ...
                bitshift(uint32(encoder0Byte(2)),8)), ...
          uint32(encoder0Byte(1)));

% Sign-extend 24-bit to 32-bit:
% left shift 8, then arithmetic right shift 8 (on int32) 
enc0 = bitshift(bitshift(int32(enc24), 8), -8);
encoder0 = double(enc0);

%% Encoder 1

%encoder1 data
encoder1Byte = [data_in(8), data_in(7), data_in(6)];

% Build 24-bit unsigned value
enc24 = bitor( ...
          bitor(bitshift(uint32(encoder1Byte(3)),16), ...
                bitshift(uint32(encoder1Byte(2)),8)), ...
          uint32(encoder1Byte(1)));

% Sign-extend from 24-bit to int32
enc1 = bitshift(bitshift(int32(enc24), 8), -8);

% Wrap counts to [0, 2047]
enc1 = mod(enc1, 2047);
if enc1 < 0
    enc1 = enc1 + 2047;
end
encoder1 = double(enc1);
